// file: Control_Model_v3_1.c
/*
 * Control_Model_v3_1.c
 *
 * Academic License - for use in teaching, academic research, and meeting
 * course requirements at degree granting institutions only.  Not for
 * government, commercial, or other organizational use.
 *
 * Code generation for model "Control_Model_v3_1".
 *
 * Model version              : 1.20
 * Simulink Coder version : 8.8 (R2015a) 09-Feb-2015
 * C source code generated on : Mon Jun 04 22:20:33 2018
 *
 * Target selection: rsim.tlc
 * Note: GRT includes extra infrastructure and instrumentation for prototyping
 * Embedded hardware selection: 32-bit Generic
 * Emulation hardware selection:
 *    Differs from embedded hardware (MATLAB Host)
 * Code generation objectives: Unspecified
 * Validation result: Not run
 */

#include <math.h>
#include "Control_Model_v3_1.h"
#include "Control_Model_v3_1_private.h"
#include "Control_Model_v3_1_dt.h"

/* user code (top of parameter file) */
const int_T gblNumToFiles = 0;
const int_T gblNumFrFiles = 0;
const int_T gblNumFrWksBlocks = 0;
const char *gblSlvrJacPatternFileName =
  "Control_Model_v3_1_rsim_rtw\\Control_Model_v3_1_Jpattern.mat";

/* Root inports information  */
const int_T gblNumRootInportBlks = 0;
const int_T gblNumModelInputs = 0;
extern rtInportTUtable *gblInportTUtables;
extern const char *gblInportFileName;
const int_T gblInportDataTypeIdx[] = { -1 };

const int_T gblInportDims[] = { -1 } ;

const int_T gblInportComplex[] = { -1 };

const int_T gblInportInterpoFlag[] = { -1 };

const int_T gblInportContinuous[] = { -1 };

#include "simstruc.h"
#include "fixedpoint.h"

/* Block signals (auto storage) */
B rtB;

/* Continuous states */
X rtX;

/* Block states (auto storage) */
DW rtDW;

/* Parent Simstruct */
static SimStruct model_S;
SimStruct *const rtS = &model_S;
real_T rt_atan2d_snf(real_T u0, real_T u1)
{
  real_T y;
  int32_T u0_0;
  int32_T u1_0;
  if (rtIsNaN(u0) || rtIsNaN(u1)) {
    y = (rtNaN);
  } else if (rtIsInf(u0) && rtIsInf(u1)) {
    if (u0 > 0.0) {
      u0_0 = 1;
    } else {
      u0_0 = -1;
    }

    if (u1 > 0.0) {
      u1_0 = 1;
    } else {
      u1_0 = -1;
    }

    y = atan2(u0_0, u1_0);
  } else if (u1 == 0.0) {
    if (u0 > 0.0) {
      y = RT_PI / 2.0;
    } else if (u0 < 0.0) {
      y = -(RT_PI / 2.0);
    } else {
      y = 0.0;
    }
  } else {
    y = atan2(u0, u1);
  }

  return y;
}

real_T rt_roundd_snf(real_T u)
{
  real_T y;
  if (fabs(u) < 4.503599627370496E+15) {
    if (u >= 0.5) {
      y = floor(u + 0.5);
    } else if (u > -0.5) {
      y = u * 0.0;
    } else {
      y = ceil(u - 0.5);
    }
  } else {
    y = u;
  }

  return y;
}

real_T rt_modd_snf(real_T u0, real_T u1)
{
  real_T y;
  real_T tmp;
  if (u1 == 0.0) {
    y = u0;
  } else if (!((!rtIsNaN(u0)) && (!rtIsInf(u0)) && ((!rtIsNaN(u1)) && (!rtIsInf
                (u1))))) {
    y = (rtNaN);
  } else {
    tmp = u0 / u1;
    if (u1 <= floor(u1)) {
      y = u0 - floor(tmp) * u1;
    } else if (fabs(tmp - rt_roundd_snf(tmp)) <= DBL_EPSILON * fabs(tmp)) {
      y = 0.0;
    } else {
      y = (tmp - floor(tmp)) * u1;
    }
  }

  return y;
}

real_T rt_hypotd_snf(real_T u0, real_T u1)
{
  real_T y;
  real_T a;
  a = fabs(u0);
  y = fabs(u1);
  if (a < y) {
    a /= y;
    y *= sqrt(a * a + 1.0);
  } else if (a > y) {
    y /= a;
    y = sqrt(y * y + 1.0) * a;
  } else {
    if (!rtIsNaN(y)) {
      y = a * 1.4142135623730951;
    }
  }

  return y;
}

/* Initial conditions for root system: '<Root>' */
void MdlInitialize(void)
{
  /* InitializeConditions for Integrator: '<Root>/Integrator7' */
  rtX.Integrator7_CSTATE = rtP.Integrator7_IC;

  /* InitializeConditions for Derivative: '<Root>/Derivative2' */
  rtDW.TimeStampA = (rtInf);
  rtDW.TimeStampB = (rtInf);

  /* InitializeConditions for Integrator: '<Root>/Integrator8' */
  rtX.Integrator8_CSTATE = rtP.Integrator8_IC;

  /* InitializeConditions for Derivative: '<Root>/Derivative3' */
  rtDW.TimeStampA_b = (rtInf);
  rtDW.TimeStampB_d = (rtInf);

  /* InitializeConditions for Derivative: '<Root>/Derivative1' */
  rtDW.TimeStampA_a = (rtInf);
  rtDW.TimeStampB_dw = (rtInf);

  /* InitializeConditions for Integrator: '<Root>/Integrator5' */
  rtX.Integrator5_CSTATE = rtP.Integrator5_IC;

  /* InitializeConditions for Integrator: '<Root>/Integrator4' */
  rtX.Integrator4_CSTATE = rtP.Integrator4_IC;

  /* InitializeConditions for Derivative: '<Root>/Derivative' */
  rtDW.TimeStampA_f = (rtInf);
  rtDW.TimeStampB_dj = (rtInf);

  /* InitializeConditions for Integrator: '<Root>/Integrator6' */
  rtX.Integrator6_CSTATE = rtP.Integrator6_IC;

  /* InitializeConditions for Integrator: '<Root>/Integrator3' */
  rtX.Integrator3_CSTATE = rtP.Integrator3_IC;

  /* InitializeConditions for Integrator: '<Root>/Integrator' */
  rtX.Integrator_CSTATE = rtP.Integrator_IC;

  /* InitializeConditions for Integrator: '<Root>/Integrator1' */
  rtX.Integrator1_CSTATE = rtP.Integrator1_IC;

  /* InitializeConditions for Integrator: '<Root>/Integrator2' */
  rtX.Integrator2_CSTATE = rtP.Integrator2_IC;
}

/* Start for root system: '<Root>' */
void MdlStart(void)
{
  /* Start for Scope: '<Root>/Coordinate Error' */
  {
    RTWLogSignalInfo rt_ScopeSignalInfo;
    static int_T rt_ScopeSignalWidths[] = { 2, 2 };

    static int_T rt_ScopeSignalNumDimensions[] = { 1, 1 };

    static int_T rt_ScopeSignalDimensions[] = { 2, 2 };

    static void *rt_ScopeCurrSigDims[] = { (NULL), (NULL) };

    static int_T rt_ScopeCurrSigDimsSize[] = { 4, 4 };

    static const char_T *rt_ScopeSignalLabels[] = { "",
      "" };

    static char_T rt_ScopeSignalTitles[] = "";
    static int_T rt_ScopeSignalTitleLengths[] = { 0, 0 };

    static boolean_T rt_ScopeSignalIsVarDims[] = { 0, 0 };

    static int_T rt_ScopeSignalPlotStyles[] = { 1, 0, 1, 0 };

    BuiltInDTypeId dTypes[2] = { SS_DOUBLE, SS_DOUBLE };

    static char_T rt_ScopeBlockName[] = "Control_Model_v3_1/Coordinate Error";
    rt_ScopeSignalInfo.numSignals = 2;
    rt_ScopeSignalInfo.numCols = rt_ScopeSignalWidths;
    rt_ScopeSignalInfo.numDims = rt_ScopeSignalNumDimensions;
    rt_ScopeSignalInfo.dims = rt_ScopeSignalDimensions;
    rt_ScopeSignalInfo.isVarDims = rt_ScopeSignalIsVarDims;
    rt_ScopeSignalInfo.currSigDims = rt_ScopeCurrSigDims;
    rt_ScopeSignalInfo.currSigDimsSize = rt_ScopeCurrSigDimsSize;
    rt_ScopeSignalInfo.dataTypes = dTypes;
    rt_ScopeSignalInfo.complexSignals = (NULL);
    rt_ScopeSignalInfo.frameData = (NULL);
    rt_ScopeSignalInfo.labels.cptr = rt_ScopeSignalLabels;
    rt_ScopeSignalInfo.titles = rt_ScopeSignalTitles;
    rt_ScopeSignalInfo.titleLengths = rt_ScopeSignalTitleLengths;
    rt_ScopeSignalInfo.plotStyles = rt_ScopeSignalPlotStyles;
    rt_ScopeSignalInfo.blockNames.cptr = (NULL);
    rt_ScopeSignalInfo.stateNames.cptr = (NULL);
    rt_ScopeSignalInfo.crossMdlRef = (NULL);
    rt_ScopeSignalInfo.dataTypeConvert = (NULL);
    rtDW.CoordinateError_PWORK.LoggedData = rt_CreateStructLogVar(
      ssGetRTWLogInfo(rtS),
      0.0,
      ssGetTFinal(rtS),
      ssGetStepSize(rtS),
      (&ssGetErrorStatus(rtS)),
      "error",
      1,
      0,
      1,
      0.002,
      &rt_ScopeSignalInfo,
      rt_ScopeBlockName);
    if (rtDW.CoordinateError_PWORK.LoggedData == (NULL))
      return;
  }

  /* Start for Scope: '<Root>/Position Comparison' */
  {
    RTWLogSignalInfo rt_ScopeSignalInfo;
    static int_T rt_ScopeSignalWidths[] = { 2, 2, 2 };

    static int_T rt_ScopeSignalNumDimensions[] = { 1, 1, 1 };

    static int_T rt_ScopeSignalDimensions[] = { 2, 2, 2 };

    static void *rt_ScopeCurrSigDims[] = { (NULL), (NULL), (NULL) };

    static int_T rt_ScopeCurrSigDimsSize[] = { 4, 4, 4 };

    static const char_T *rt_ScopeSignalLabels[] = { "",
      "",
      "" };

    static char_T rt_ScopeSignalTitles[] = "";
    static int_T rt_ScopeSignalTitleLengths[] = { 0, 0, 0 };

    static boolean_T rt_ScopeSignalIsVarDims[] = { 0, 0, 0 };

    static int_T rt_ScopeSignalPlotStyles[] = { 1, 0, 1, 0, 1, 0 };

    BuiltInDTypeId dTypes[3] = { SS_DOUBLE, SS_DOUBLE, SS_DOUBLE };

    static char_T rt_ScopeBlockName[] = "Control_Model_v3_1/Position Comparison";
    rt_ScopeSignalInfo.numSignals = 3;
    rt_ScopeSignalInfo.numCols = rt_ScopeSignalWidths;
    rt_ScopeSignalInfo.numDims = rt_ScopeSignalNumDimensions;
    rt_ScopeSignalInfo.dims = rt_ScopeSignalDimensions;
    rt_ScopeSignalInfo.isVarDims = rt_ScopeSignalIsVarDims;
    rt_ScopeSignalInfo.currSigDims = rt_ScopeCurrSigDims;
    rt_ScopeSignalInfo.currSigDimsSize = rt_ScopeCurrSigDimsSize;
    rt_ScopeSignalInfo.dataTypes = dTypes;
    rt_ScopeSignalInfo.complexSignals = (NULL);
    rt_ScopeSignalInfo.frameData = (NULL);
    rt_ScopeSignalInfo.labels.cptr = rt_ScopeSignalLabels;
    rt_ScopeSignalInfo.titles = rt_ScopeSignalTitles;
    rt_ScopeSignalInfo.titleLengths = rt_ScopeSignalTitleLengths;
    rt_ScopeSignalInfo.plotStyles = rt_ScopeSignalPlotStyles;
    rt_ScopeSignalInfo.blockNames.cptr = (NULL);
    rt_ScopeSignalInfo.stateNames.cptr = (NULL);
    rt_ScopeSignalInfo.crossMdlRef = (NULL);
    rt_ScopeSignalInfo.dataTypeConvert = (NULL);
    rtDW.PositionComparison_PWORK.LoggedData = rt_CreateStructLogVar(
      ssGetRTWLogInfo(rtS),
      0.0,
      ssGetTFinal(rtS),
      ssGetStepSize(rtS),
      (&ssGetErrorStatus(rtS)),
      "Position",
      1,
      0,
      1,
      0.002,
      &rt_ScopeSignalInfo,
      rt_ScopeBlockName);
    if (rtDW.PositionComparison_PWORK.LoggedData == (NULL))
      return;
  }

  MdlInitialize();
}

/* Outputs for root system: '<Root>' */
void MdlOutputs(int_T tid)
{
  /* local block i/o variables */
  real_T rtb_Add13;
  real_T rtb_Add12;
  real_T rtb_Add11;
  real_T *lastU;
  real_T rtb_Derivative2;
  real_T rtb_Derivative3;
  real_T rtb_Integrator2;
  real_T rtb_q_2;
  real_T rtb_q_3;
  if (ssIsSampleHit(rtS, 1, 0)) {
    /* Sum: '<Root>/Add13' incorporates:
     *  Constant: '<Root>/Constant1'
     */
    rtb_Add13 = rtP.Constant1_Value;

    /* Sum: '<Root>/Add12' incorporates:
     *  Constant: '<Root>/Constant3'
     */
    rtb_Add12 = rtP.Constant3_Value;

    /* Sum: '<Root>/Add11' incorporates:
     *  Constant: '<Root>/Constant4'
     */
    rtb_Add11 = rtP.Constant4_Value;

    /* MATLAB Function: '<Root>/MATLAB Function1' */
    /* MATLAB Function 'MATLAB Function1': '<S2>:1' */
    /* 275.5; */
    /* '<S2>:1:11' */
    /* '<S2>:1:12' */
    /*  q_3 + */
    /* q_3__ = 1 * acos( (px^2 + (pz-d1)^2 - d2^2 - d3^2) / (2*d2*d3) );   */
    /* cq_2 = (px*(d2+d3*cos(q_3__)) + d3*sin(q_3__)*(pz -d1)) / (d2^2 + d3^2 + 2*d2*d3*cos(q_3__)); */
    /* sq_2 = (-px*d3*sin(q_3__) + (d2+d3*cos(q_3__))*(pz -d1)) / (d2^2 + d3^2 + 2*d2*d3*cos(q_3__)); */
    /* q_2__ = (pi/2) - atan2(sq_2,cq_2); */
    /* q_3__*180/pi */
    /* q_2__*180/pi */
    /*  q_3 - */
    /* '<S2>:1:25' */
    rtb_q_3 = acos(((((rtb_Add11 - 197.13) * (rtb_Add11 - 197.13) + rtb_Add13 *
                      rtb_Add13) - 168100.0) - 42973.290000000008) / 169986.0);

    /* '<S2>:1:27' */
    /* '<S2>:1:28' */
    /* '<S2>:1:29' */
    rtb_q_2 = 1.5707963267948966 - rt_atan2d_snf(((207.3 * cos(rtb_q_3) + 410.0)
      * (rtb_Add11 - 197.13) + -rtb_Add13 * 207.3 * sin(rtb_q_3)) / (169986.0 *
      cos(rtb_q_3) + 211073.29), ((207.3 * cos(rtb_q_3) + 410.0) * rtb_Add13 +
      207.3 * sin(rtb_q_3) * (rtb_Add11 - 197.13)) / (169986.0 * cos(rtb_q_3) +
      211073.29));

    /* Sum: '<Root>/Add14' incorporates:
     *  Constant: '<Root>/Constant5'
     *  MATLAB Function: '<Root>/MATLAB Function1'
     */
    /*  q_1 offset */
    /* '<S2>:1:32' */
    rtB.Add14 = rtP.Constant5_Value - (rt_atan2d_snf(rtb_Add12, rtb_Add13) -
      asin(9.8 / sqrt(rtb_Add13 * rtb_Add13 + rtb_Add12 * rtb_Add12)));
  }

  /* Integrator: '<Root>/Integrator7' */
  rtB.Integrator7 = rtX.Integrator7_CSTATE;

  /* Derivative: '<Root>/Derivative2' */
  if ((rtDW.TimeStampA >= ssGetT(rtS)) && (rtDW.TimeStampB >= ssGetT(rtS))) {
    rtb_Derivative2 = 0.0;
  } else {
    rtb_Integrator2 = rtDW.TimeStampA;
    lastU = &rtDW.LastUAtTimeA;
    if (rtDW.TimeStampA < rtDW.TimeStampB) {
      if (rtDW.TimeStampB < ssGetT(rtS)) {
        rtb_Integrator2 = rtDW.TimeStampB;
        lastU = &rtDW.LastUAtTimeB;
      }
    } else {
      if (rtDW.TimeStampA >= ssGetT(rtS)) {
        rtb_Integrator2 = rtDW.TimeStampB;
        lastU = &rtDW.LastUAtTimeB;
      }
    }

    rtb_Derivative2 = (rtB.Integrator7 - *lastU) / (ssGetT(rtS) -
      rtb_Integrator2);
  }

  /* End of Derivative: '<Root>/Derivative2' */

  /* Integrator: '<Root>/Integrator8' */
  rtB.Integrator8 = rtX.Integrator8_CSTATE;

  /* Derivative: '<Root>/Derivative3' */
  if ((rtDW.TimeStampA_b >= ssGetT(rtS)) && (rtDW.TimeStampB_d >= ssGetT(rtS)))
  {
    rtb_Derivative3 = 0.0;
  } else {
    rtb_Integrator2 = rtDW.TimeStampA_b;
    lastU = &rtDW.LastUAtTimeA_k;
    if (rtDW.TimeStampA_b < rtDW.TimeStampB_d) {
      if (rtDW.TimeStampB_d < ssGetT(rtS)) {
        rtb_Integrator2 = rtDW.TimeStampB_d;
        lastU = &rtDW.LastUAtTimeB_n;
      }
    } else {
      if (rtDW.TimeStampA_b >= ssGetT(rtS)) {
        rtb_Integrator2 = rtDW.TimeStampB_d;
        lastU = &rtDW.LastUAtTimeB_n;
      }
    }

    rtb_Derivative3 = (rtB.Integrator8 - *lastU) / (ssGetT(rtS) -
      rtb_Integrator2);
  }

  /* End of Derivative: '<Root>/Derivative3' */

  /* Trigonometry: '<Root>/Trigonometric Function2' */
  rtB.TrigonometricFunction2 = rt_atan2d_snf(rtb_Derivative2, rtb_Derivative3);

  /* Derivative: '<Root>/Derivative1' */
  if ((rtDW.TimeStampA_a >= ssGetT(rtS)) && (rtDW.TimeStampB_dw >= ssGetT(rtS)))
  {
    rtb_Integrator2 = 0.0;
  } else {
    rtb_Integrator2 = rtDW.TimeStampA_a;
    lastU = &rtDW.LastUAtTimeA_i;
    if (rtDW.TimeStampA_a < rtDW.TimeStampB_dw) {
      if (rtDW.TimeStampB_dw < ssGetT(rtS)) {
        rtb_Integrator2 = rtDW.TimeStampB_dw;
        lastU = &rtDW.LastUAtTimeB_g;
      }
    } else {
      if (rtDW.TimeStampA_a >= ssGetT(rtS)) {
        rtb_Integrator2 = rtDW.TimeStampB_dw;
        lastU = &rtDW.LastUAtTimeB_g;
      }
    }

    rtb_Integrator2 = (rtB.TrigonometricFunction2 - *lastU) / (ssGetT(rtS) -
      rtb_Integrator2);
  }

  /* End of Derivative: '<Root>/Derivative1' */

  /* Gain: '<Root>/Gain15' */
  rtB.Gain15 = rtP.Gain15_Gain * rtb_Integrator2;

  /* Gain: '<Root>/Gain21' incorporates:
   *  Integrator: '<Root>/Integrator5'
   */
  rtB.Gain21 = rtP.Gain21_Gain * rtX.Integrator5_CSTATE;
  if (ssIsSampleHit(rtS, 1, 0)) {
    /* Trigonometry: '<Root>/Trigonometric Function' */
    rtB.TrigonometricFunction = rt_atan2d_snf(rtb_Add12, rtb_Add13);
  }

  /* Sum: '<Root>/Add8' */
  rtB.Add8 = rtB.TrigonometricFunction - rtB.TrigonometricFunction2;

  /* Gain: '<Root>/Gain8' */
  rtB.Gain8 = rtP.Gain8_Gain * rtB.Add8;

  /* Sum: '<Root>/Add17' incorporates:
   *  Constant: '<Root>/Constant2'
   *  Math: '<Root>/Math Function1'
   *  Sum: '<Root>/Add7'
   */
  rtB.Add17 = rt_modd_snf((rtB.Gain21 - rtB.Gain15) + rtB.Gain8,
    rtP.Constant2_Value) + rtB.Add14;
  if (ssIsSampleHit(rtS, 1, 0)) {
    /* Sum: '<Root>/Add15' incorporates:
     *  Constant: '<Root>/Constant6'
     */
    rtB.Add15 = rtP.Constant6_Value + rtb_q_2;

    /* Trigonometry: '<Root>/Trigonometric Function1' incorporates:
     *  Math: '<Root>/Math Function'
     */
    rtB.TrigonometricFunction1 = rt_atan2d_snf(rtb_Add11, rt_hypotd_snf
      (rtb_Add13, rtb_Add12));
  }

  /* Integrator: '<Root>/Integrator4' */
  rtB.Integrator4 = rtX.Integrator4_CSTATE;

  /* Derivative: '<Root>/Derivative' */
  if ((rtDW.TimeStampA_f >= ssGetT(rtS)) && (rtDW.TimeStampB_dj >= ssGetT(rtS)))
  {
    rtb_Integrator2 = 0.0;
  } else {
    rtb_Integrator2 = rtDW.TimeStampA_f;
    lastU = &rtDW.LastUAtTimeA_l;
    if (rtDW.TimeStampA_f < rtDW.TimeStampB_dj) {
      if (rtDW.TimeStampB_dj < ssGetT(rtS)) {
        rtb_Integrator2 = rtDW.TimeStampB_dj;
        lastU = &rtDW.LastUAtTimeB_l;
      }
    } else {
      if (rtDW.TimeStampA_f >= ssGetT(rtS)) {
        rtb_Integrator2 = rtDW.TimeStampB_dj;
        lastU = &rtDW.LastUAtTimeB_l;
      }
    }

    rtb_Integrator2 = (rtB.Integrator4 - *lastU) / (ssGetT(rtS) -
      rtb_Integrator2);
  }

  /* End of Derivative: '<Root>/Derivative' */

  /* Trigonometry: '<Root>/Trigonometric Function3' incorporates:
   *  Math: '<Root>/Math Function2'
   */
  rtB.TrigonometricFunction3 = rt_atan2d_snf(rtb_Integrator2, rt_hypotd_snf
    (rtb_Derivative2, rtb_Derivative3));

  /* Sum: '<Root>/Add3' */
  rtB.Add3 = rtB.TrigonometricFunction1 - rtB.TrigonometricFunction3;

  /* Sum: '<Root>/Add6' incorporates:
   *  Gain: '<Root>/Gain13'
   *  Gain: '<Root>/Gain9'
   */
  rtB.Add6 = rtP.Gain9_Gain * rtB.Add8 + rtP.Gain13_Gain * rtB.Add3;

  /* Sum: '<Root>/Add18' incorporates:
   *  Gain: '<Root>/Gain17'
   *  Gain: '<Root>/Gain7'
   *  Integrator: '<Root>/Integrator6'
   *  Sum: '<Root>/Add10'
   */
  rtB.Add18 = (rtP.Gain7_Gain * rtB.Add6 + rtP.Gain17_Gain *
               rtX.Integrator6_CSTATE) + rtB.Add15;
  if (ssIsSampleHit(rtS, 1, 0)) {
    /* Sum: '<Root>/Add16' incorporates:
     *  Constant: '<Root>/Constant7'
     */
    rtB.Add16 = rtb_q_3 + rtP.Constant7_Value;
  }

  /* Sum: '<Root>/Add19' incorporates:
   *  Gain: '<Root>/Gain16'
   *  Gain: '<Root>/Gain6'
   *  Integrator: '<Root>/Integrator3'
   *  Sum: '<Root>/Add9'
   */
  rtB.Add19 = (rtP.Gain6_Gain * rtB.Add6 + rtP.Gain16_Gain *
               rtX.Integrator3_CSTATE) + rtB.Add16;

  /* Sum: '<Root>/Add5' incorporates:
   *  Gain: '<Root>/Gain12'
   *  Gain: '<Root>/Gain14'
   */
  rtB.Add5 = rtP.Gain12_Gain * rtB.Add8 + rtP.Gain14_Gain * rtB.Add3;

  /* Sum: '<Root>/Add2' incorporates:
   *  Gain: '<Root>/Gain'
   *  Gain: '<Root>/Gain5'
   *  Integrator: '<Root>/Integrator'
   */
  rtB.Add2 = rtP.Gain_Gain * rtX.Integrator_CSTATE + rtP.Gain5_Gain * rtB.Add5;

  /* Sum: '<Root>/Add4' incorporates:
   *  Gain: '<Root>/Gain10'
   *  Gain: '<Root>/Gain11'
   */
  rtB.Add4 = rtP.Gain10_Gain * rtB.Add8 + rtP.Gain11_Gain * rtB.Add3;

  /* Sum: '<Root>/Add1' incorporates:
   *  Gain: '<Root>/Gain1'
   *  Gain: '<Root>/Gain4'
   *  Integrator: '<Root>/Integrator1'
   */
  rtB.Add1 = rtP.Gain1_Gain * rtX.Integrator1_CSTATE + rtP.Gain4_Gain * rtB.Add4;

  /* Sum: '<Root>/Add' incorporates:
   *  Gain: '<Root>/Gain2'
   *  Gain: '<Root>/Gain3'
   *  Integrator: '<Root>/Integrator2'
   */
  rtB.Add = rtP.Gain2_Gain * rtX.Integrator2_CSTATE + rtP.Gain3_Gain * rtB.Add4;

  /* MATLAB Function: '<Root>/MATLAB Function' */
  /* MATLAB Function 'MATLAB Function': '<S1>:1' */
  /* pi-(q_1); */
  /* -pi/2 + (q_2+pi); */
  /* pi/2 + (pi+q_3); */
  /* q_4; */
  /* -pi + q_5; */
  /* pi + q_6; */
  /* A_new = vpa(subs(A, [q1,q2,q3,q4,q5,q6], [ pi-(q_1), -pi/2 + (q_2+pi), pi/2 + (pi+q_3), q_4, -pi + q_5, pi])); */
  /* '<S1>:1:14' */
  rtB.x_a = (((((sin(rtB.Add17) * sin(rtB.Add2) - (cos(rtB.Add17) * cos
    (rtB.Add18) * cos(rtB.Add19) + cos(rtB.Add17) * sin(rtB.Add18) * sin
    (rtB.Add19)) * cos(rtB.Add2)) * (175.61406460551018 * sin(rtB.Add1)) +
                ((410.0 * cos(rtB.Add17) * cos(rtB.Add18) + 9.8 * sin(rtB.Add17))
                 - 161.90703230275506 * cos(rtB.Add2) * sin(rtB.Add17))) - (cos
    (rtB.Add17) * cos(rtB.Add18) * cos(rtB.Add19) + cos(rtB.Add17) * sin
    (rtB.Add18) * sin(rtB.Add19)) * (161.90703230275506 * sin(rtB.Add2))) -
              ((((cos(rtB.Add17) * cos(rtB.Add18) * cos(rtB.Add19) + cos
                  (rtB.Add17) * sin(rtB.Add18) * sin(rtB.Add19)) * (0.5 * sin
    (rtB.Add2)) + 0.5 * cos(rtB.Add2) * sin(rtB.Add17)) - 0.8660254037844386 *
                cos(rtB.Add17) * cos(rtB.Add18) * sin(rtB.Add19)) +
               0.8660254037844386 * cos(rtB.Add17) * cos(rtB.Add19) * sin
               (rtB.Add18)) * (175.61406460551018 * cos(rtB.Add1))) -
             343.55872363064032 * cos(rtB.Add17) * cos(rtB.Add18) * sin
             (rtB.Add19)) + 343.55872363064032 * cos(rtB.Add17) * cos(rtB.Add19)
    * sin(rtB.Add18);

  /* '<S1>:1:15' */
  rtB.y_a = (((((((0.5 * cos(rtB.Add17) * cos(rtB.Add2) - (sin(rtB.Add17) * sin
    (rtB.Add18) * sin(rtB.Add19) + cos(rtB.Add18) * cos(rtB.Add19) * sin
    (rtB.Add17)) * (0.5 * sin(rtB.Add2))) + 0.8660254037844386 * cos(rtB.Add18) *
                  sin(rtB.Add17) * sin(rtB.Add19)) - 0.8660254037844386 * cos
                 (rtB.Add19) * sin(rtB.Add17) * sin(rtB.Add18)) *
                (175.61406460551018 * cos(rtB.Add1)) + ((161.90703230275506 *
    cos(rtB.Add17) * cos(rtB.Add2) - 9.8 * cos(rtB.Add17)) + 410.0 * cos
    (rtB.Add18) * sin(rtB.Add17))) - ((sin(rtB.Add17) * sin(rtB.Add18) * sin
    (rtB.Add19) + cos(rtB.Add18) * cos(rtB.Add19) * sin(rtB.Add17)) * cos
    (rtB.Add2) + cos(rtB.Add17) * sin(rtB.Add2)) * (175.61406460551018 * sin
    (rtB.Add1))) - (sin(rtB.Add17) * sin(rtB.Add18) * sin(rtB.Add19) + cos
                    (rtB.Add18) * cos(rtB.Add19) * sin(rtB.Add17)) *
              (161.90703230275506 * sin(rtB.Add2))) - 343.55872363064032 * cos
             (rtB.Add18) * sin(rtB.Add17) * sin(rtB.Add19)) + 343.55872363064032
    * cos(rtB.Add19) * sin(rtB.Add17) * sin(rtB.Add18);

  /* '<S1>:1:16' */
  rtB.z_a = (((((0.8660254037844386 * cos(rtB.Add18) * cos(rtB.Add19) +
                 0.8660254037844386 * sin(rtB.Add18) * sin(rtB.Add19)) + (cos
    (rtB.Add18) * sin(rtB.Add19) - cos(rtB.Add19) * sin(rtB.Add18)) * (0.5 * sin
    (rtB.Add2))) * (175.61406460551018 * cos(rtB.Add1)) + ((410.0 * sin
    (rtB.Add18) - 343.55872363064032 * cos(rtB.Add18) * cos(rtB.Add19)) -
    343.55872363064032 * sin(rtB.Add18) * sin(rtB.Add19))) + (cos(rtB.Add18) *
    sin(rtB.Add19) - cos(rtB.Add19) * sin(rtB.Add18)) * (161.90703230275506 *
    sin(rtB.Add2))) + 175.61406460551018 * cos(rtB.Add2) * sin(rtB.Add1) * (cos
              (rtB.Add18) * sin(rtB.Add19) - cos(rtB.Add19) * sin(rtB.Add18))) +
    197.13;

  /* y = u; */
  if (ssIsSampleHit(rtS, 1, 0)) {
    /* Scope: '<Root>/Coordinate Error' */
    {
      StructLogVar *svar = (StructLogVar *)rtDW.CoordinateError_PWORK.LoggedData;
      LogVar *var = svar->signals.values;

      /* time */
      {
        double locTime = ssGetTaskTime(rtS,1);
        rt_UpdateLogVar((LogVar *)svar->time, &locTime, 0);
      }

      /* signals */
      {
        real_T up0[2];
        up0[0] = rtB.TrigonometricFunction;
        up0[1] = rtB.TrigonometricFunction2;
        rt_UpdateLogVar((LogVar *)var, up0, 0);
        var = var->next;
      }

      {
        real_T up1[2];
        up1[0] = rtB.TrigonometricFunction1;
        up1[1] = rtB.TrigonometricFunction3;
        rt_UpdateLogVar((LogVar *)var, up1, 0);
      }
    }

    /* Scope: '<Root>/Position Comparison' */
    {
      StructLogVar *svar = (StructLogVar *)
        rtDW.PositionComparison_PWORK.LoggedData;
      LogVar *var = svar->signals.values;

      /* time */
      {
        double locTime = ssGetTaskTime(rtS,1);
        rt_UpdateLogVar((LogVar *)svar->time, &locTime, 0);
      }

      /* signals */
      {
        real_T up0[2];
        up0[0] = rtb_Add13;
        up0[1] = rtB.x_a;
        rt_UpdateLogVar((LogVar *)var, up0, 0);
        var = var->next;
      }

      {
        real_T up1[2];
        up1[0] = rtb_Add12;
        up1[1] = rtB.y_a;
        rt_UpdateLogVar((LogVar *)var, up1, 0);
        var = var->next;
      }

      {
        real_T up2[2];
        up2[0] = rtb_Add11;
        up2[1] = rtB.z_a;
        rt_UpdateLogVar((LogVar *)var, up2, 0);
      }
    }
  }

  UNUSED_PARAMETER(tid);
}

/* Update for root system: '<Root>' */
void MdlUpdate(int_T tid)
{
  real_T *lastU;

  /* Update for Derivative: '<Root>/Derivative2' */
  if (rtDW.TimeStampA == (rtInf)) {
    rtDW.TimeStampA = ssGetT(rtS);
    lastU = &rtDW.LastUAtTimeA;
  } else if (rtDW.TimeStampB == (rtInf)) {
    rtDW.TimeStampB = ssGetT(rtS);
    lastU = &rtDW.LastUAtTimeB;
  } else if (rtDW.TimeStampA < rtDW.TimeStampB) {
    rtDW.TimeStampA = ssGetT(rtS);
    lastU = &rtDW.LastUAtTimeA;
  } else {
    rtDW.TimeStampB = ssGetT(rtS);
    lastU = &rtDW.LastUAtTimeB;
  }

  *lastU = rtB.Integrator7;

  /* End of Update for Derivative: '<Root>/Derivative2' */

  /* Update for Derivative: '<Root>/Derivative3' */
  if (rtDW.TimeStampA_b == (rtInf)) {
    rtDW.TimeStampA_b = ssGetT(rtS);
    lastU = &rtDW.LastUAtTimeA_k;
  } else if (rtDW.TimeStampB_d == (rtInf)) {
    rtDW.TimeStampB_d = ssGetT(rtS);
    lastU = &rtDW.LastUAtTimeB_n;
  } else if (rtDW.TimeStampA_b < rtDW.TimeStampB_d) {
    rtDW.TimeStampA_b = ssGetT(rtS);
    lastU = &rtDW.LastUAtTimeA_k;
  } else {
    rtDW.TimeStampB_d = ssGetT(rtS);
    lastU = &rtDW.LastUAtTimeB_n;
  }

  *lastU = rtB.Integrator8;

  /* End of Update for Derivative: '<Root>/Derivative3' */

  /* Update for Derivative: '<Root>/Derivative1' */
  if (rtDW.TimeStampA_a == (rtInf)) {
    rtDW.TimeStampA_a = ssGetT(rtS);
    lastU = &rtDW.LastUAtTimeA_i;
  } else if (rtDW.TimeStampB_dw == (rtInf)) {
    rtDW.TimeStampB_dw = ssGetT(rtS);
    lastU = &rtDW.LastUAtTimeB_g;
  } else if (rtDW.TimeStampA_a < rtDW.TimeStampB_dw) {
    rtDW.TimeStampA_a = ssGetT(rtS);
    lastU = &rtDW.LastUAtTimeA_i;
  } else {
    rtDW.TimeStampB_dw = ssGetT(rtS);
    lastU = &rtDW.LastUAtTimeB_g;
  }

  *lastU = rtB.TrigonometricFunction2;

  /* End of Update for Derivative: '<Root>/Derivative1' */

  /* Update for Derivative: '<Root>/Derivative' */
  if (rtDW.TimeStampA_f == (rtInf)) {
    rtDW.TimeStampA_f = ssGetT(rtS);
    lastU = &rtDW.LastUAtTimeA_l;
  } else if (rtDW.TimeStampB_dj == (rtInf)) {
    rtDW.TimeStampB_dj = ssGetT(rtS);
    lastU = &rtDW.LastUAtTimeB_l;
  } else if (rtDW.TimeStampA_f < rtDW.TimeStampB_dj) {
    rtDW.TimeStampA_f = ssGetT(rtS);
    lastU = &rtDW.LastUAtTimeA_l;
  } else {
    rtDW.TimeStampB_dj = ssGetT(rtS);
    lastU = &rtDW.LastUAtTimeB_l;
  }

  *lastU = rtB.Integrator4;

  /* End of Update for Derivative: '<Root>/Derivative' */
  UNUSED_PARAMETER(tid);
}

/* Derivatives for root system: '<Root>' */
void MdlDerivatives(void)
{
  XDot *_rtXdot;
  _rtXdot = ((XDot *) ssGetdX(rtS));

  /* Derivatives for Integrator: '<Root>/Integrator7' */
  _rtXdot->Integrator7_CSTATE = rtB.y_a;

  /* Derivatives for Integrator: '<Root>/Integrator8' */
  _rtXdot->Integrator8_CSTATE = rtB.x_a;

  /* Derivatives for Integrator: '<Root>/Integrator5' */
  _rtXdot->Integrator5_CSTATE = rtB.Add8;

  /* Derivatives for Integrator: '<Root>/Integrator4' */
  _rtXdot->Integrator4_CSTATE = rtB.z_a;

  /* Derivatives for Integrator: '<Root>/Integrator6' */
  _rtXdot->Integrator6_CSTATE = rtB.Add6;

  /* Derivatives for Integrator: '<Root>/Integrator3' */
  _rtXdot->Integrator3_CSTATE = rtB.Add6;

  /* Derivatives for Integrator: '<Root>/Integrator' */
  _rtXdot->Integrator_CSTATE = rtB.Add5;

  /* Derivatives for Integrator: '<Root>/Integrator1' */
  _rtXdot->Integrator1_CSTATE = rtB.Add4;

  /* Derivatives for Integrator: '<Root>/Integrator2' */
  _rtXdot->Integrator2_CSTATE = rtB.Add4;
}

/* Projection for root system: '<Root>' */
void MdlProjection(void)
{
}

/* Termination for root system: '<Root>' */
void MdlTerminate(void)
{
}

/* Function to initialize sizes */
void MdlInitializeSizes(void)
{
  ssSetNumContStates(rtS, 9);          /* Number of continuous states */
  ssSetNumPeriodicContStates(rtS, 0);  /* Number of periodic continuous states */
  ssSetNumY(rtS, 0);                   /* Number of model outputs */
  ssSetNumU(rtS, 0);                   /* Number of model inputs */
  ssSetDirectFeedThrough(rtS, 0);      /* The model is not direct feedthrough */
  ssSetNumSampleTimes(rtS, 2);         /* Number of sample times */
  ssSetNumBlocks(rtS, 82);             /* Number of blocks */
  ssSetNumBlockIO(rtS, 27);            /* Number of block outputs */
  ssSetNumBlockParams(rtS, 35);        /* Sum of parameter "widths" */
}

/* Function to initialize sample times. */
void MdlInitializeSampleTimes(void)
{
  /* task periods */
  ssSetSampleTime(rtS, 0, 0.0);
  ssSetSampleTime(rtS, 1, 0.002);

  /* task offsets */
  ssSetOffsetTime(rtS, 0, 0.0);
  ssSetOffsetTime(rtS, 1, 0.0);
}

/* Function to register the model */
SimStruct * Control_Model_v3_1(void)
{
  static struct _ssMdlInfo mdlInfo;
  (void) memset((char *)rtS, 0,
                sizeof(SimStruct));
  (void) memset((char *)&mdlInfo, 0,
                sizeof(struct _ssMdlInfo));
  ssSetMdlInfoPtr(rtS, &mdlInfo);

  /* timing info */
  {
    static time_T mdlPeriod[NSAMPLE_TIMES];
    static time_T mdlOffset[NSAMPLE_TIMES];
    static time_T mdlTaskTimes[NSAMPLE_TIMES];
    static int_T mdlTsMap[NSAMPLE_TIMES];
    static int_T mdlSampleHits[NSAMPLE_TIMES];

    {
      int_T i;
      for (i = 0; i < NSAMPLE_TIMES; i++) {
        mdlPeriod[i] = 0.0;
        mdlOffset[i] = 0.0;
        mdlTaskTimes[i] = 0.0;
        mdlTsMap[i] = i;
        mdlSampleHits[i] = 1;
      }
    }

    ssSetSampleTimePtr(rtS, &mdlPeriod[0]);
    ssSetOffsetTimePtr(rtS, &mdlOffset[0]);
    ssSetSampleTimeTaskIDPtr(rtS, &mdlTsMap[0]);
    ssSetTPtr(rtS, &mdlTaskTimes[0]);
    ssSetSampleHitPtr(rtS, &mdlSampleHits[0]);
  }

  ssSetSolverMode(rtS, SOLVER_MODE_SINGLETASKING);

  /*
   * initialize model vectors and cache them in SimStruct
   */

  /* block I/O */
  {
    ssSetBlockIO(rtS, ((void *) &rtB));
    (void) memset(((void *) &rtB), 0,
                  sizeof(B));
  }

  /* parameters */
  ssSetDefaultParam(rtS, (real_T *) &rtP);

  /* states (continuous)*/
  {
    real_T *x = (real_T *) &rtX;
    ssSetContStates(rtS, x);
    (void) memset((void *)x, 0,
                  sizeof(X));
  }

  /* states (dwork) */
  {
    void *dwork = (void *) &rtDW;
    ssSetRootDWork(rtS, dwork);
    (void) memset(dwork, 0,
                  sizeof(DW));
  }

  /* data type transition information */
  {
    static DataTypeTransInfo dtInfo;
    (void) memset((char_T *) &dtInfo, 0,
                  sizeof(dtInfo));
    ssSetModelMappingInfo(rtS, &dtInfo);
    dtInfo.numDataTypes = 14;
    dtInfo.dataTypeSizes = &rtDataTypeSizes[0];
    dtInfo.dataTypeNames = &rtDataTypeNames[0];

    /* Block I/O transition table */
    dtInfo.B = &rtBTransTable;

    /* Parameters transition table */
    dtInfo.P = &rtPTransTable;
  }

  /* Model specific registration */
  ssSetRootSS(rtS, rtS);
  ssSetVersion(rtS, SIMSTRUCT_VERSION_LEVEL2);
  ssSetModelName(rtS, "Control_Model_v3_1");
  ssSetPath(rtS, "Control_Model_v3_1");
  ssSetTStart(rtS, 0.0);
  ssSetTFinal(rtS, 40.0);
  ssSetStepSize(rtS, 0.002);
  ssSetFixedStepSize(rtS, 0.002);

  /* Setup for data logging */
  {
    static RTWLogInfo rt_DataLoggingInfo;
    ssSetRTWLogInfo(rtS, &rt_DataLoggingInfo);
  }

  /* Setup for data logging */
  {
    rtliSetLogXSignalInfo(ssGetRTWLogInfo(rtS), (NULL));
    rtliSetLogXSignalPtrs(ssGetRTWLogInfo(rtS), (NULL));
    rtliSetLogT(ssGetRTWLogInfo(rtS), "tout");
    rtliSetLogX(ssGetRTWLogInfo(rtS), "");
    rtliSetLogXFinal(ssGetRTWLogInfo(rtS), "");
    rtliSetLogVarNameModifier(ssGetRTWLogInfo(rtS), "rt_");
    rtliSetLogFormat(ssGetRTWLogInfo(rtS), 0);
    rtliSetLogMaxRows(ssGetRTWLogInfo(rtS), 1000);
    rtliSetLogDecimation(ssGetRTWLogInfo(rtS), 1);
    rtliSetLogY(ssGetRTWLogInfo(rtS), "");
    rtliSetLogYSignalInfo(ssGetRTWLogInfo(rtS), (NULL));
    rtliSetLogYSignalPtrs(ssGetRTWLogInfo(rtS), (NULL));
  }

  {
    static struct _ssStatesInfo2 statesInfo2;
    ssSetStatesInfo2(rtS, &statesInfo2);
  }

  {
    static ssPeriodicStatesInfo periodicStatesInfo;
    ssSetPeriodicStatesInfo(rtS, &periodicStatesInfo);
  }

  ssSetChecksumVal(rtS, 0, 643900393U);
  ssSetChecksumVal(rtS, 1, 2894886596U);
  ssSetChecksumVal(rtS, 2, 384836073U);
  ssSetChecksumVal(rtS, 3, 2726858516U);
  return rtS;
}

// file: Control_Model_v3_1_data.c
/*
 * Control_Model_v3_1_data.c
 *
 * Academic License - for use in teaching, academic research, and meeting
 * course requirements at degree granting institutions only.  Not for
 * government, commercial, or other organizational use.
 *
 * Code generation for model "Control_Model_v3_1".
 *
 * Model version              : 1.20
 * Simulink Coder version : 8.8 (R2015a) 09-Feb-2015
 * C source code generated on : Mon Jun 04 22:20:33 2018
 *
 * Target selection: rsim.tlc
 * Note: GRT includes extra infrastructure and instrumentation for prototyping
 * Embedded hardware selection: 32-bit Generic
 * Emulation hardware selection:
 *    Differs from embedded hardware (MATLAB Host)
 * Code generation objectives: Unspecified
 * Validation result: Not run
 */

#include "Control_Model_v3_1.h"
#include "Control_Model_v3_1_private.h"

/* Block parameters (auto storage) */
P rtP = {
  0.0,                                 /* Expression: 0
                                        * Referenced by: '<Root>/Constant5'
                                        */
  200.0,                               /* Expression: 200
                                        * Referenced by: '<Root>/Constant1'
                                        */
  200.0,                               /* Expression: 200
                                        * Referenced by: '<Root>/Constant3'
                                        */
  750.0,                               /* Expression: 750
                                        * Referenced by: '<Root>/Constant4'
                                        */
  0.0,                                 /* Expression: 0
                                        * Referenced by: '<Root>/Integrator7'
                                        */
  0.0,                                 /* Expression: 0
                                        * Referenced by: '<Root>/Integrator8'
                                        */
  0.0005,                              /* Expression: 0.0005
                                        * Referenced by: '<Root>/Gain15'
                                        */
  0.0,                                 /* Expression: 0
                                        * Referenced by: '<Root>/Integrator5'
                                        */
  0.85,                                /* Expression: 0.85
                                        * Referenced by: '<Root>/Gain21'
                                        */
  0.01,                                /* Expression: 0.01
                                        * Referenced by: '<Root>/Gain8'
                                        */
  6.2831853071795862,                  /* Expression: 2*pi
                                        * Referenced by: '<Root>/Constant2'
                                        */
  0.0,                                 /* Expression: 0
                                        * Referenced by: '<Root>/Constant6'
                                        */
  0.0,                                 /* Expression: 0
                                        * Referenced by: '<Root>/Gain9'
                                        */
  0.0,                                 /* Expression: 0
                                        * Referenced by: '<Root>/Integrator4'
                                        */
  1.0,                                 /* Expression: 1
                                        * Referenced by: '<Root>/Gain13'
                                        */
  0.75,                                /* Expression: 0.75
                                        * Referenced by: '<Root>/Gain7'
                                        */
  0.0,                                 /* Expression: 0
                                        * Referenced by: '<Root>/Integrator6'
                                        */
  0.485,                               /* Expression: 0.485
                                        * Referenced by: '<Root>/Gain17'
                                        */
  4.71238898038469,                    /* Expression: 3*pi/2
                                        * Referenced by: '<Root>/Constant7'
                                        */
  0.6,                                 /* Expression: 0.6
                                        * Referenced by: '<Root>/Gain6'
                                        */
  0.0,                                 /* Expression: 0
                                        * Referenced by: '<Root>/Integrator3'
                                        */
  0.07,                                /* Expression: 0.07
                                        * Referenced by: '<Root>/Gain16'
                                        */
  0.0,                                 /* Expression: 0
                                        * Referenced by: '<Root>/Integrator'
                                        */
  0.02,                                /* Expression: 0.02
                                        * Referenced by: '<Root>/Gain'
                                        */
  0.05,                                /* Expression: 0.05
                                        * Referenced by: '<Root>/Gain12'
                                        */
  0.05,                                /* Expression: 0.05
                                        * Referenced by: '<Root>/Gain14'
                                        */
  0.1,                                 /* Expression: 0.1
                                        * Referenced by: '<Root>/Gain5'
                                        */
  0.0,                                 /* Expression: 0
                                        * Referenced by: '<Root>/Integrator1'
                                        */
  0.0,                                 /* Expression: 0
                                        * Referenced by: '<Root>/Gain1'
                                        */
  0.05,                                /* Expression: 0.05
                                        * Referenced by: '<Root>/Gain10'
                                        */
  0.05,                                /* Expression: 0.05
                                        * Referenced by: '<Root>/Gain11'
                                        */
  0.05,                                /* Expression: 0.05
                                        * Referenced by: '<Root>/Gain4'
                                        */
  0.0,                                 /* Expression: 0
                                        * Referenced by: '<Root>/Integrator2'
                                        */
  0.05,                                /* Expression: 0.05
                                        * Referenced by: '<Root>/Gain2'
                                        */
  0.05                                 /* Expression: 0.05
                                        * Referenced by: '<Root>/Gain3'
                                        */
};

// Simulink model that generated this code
simulink model "Control_Model_v3_1"  (R2015a)
settings: Solver=ode1  StartTime=0.0  StopTime=40  FixedStep=0.002  MaxStep=0.01  MinStep=0.01  RelTol=1e-3

== system Control_Model_v3_1 ==
  Actual Position : Scope
  Add{,1..2,4..6,9..10,15..19} (13 alike) : Sum
  Add11 : Sum  Inputs=+++
  Add12 : Sum  Inputs=+++
  Add13 : Sum  Inputs=+++
  Add14 : Sum  Inputs=+-
  Add3 : Sum  Inputs=+-
  Add7 : Sum  Inputs=-++
  Add8 : Sum  Inputs=+-
  Constant1 : Constant  Value=200
  Constant2 : Constant  Value=2*pi
  Constant3 : Constant  Value=200
  Constant4 : Constant  Value=750
  Constant5 : Constant  Value=0
  Constant6 : Constant  Value=0
  Constant7 : Constant  Value=3*pi/2
  Coordinate Error : Scope  NumInputPorts=2
  Coordinate Error1 : Scope  NumInputPorts=3
  Derivative{,1..3} (4 alike) : Derivative
  Gain : Gain  Gain=0.02
  Gain1 : Gain  Gain=0
  Gain{2..4,10..12,14} (7 alike) : Gain  Gain=0.05
  Gain13 : Gain
  Gain15 : Gain  Gain=0.0005
  Gain16 : Gain  Gain=0.07
  Gain17 : Gain  Gain=0.485
  Gain21 : Gain  Gain=0.85
  Gain5 : Gain  Gain=0.1
  Gain6 : Gain  Gain=0.6
  Gain7 : Gain  Gain=0.75
  Gain8 : Gain  Gain=0.01
  Gain9 : Gain  Gain=0
  Integrator{,1..8} (9 alike) : Integrator
  MATLAB Function : MATLAB Function  TreatAsAtomicUnit=on
  MATLAB Function1 : MATLAB Function  TreatAsAtomicUnit=on
  Math Function : Math  Operator=hypot  SaturateOnIntegerOverflow=on
  Math Function1 : Math  Operator=mod  SaturateOnIntegerOverflow=on
  Math Function2 : Math  Operator=hypot  SaturateOnIntegerOverflow=on
  Mux : Mux  Inputs=3
  Mux{1..8} (8 alike) : Mux  Inputs=2
  Position Comparison : Scope  NumInputPorts=3
  Step : Step  After=-60  SampleTime=0
  Step1 : Step  After=-50  SampleTime=0
  Step2 : Step  After=0  SampleTime=0
  Step3 : Step  After=100  SampleTime=0
  Trigonometric Function{,1..3} (4 alike) : Trigonometry  Operator=atan2
  q_1 correction : Scope
  q_1 correction1 : Scope  NumInputPorts=3
  q_1 correction2 : Scope  NumInputPorts=2
  q_2 correction1 : Scope
  q_3 correction : Scope
  q_4 correction : Scope
  q_5 correction1 : Scope
  q_6 correction2 : Scope
  wires:
  Integrator/1 -> Gain/1
  Integrator1/1 -> Gain1/1
  Integrator2/1 -> Gain2/1
  Gain2/1 -> Add/1
  Gain3/1 -> Add/2
  Add/1 -> MATLAB Function/6(q_6), q_6 correction2/1
  Gain1/1 -> Add1/1
  Add1/1 -> MATLAB Function/5(q_5), q_5 correction1/1
  Gain4/1 -> Add1/2
  Add2/1 -> MATLAB Function/4(q_4), q_4 correction/1
  Gain/1 -> Add2/1
  Gain5/1 -> Add2/2
  Add5/1 -> Gain5/1, Integrator/1
  Add6/1 -> Integrator3/1, Gain6/1, Integrator6/1, Gain7/1
  Add11/1 -> Mux8/1, Coordinate Error1/3, MATLAB Function1/3(pz), Trigonometric Function1/1
  MATLAB Function/1(x_a) -> Integrator8/1, Mux/1, Mux7/2
  Gain10/1 -> Add4/1
  Gain14/1 -> Add5/2
  Gain6/1 -> Add9/1
  Derivative/1 -> Trigonometric Function3/1
  Integrator5/1 -> Gain21/1
  Gain21/1 -> q_1 correction1/2, Add7/2
  Add7/1 -> Math Function1/1
  Gain8/1 -> q_1 correction1/1, Add7/3
  Gain12/1 -> Add5/1
  Gain13/1 -> Add6/2
  Gain9/1 -> Add6/1
  Add3/1 -> Gain11/1, Gain14/1, Gain13/1, q_1 correction2/2
  Math Function/1 -> Trigonometric Function1/2
  Derivative1/1 -> Gain15/1
  Gain15/1 -> Add7/1, q_1 correction1/3
  Constant2/1 -> Math Function1/2
  Integrator3/1 -> Gain16/1
  Gain16/1 -> Add9/2
  Integrator6/1 -> Gain17/1
  Gain7/1 -> Add10/1
  Gain17/1 -> Add10/2
  Integrator8/1 -> Derivative3/1
  Derivative3/1 -> Math Function2/2, Trigonometric Function2/2
  Mux/1 -> Actual Position/1
  Mux1/1 -> Coordinate Error/1
  Derivative2/1 -> Math Function2/1, Trigonometric Function2/1
  Trigonometric Function/1 -> Add8/1, Mux1/1
  Trigonometric Function2/1 -> Add8/2, Derivative1/1, Mux1/2
  Math Function2/1 -> Trigonometric Function3/2
  Trigonometric Function3/1 -> Mux2/2, Add3/2
  Trigonometric Function1/1 -> Add3/1, Mux2/1
  Mux2/1 -> Coordinate Error/2
  Integrator4/1 -> Derivative/1
  MATLAB Function/3(z_a) -> Integrator4/1, Mux/3, Mux8/2
  Integrator7/1 -> Derivative2/1
  Add8/1 -> Gain9/1, Gain12/1, Gain10/1, q_1 correction2/1, Integrator5/1, Gain8/1
  Step2/1 -> ?
  Step3/1 -> ?
  Constant4/1 -> Add11/3
  Step1/1 -> ?
  Constant3/1 -> Add12/1
  Step/1 -> ?
  Constant1/1 -> Add13/1
  MATLAB Function1/1(q_1) -> Add14/2
  Constant5/1 -> Add14/1
  MATLAB Function1/2(q_2) -> Add15/2
  Constant6/1 -> Add15/1
  MATLAB Function1/3(q_3) -> Add16/1
  Constant7/1 -> Add16/2
  Add14/1 -> Add17/1, Mux3/1
  Add16/1 -> Mux5/1, Add19/1
  Math Function1/1 -> Add17/2
  Add17/1 -> Mux3/2, MATLAB Function/1(q_1)
  Add18/1 -> MATLAB Function/2(q_2), Mux4/2
  Add10/1 -> Add18/2
  Add9/1 -> Add19/2
  Add19/1 -> MATLAB Function/3(q_3), Mux5/2
  Mux3/1 -> q_1 correction/1
  Mux4/1 -> q_2 correction1/1
  Mux5/1 -> q_3 correction/1
  Add15/1 -> Add18/1, Mux4/1
  Add13/1 -> Mux7/1, Coordinate Error1/1, MATLAB Function1/1(px), Trigonometric Function/2, Math Function/1
  Mux7/1 -> Position Comparison/1
  MATLAB Function/2(y_a) -> Integrator7/1, Mux/2, Mux6/2
  Add12/1 -> Math Function/2, Trigonometric Function/1, MATLAB Function1/2(py), Mux6/1, Coordinate Error1/2
  Mux6/1 -> Position Comparison/2
  Mux8/1 -> Position Comparison/3
  Gain11/1 -> Add4/2
  Add4/1 -> Gain3/1, Integrator1/1, Gain4/1, Integrator2/1

== matlab function Control_Model_v3_1/MATLAB Function1 ==
function [q_1, q_2, q_3] = fcn( px, py, pz)
%#codegen

D1 = 197.13;%275.5;
D2 = 410;
D3 = 207.3;
D4 = 74.1;
D5 = 74.1;
D6 = 160.0;
e2 = 9.8;
d1 = 197.13;
d2 = D2;
d3 = D3;

% q_3 +
%q_3__ = 1 * acos( (px^2 + (pz-d1)^2 - d2^2 - d3^2) / (2*d2*d3) );  

%cq_2 = (px*(d2+d3*cos(q_3__)) + d3*sin(q_3__)*(pz -d1)) / (d2^2 + d3^2 + 2*d2*d3*cos(q_3__));
%sq_2 = (-px*d3*sin(q_3__) + (d2+d3*cos(q_3__))*(pz -d1)) / (d2^2 + d3^2 + 2*d2*d3*cos(q_3__));
%q_2__ = (pi/2) - atan2(sq_2,cq_2);
%q_3__*180/pi
%q_2__*180/pi
% q_3 -

q_3 = 1 * acos( (px^2 + (pz-d1)^2 - d2^2 - d3^2) / (2*d2*d3) );  

cq_2 = (px*(d2+d3*cos(q_3)) + d3*sin(q_3)*(pz -d1)) / (d2^2 + d3^2 + 2*d2*d3*cos(q_3));
sq_2 = (-px*d3*sin(q_3) + (d2+d3*cos(q_3))*(pz -d1)) / (d2^2 + d3^2 + 2*d2*d3*cos(q_3));
q_2 = (pi/2) - atan2(sq_2,cq_2);

% q_1 offset
q_1 = atan2((py), px) - asin(e2 / ((px^2 + py^2)^.5));

== matlab function Control_Model_v3_1/MATLAB Function ==
function [x_a, y_a, z_a] = fcn(q_1, q_2, q_3, q_4, q_5, q_6)
%#codegen

q1 = q_1;%pi-(q_1);
q2 = q_2;%-pi/2 + (q_2+pi);
q3 = q_3;%pi/2 + (pi+q_3);
q4 = q_4;%q_4;
q5 = q_5;%-pi + q_5;
q6 = q_6;%pi + q_6;

%A_new = vpa(subs(A, [q1,q2,q3,q4,q5,q6], [ pi-(q_1), -pi/2 + (q_2+pi), pi/2 + (pi+q_3), q_4, -pi + q_5, pi]));

x_a = 9.8*sin(q1) + 410.0*cos(q1)*cos(q2) - 161.90703230275506147226218323136*cos(q4)*sin(q1) + 175.614064605510166451876962007*sin(q5)*(1.0*sin(q1)*sin(q4) - cos(q4)*(cos(q1)*cos(q2)*cos(q3) + cos(q1)*sin(q2)*sin(q3))) - 161.90703230275506147226218323136*sin(q4)*(cos(q1)*cos(q2)*cos(q3) + cos(q1)*sin(q2)*sin(q3)) - 175.614064605510166451876962007*cos(q5)*(0.5*cos(q4)*sin(q1) + 0.5*sin(q4)*(cos(q1)*cos(q2)*cos(q3) + cos(q1)*sin(q2)*sin(q3)) - 0.86602540378443864676372317075294*cos(q1)*cos(q2)*sin(q3) + 0.86602540378443864676372317075294*cos(q1)*cos(q3)*sin(q2)) - 343.55872363064032981583295622841*cos(q1)*cos(q2)*sin(q3) + 343.55872363064032981583295622841*cos(q1)*cos(q3)*sin(q2); 
y_a = 161.90703230275506147226218323136*cos(q1)*cos(q4) - 9.8*cos(q1) + 410.0*cos(q2)*sin(q1) + 175.614064605510166451876962007*cos(q5)*(0.5*cos(q1)*cos(q4) - 0.5*sin(q4)*(sin(q1)*sin(q2)*sin(q3) + cos(q2)*cos(q3)*sin(q1)) + 0.86602540378443864676372317075294*cos(q2)*sin(q1)*sin(q3) - 0.86602540378443864676372317075294*cos(q3)*sin(q1)*sin(q2)) - 175.614064605510166451876962007*sin(q5)*(1.0*cos(q1)*sin(q4) + cos(q4)*(sin(q1)*sin(q2)*sin(q3) + cos(q2)*cos(q3)*sin(q1))) - 161.90703230275506147226218323136*sin(q4)*(sin(q1)*sin(q2)*sin(q3) + cos(q2)*cos(q3)*sin(q1)) - 343.55872363064032981583295622841*cos(q2)*sin(q1)*sin(q3) + 343.55872363064032981583295622841*cos(q3)*sin(q1)*sin(q2);
z_a = 410.0*sin(q2) - 343.55872363064032981583295622841*cos(q2)*cos(q3) - 343.55872363064032981583295622841*sin(q2)*sin(q3) + 175.614064605510166451876962007*cos(q5)*(0.86602540378443864676372317075294*cos(q2)*cos(q3) + 0.86602540378443864676372317075294*sin(q2)*sin(q3) + 0.5*sin(q4)*(1.0*cos(q2)*sin(q3) - 1.0*cos(q3)*sin(q2))) + 161.90703230275506147226218323136*sin(q4)*(1.0*cos(q2)*sin(q3) - 1.0*cos(q3)*sin(q2)) + 175.614064605510166451876962007*cos(q4)*sin(q5)*(1.0*cos(q2)*sin(q3) - 1.0*cos(q3)*sin(q2)) + 197.13;

%y = u;
